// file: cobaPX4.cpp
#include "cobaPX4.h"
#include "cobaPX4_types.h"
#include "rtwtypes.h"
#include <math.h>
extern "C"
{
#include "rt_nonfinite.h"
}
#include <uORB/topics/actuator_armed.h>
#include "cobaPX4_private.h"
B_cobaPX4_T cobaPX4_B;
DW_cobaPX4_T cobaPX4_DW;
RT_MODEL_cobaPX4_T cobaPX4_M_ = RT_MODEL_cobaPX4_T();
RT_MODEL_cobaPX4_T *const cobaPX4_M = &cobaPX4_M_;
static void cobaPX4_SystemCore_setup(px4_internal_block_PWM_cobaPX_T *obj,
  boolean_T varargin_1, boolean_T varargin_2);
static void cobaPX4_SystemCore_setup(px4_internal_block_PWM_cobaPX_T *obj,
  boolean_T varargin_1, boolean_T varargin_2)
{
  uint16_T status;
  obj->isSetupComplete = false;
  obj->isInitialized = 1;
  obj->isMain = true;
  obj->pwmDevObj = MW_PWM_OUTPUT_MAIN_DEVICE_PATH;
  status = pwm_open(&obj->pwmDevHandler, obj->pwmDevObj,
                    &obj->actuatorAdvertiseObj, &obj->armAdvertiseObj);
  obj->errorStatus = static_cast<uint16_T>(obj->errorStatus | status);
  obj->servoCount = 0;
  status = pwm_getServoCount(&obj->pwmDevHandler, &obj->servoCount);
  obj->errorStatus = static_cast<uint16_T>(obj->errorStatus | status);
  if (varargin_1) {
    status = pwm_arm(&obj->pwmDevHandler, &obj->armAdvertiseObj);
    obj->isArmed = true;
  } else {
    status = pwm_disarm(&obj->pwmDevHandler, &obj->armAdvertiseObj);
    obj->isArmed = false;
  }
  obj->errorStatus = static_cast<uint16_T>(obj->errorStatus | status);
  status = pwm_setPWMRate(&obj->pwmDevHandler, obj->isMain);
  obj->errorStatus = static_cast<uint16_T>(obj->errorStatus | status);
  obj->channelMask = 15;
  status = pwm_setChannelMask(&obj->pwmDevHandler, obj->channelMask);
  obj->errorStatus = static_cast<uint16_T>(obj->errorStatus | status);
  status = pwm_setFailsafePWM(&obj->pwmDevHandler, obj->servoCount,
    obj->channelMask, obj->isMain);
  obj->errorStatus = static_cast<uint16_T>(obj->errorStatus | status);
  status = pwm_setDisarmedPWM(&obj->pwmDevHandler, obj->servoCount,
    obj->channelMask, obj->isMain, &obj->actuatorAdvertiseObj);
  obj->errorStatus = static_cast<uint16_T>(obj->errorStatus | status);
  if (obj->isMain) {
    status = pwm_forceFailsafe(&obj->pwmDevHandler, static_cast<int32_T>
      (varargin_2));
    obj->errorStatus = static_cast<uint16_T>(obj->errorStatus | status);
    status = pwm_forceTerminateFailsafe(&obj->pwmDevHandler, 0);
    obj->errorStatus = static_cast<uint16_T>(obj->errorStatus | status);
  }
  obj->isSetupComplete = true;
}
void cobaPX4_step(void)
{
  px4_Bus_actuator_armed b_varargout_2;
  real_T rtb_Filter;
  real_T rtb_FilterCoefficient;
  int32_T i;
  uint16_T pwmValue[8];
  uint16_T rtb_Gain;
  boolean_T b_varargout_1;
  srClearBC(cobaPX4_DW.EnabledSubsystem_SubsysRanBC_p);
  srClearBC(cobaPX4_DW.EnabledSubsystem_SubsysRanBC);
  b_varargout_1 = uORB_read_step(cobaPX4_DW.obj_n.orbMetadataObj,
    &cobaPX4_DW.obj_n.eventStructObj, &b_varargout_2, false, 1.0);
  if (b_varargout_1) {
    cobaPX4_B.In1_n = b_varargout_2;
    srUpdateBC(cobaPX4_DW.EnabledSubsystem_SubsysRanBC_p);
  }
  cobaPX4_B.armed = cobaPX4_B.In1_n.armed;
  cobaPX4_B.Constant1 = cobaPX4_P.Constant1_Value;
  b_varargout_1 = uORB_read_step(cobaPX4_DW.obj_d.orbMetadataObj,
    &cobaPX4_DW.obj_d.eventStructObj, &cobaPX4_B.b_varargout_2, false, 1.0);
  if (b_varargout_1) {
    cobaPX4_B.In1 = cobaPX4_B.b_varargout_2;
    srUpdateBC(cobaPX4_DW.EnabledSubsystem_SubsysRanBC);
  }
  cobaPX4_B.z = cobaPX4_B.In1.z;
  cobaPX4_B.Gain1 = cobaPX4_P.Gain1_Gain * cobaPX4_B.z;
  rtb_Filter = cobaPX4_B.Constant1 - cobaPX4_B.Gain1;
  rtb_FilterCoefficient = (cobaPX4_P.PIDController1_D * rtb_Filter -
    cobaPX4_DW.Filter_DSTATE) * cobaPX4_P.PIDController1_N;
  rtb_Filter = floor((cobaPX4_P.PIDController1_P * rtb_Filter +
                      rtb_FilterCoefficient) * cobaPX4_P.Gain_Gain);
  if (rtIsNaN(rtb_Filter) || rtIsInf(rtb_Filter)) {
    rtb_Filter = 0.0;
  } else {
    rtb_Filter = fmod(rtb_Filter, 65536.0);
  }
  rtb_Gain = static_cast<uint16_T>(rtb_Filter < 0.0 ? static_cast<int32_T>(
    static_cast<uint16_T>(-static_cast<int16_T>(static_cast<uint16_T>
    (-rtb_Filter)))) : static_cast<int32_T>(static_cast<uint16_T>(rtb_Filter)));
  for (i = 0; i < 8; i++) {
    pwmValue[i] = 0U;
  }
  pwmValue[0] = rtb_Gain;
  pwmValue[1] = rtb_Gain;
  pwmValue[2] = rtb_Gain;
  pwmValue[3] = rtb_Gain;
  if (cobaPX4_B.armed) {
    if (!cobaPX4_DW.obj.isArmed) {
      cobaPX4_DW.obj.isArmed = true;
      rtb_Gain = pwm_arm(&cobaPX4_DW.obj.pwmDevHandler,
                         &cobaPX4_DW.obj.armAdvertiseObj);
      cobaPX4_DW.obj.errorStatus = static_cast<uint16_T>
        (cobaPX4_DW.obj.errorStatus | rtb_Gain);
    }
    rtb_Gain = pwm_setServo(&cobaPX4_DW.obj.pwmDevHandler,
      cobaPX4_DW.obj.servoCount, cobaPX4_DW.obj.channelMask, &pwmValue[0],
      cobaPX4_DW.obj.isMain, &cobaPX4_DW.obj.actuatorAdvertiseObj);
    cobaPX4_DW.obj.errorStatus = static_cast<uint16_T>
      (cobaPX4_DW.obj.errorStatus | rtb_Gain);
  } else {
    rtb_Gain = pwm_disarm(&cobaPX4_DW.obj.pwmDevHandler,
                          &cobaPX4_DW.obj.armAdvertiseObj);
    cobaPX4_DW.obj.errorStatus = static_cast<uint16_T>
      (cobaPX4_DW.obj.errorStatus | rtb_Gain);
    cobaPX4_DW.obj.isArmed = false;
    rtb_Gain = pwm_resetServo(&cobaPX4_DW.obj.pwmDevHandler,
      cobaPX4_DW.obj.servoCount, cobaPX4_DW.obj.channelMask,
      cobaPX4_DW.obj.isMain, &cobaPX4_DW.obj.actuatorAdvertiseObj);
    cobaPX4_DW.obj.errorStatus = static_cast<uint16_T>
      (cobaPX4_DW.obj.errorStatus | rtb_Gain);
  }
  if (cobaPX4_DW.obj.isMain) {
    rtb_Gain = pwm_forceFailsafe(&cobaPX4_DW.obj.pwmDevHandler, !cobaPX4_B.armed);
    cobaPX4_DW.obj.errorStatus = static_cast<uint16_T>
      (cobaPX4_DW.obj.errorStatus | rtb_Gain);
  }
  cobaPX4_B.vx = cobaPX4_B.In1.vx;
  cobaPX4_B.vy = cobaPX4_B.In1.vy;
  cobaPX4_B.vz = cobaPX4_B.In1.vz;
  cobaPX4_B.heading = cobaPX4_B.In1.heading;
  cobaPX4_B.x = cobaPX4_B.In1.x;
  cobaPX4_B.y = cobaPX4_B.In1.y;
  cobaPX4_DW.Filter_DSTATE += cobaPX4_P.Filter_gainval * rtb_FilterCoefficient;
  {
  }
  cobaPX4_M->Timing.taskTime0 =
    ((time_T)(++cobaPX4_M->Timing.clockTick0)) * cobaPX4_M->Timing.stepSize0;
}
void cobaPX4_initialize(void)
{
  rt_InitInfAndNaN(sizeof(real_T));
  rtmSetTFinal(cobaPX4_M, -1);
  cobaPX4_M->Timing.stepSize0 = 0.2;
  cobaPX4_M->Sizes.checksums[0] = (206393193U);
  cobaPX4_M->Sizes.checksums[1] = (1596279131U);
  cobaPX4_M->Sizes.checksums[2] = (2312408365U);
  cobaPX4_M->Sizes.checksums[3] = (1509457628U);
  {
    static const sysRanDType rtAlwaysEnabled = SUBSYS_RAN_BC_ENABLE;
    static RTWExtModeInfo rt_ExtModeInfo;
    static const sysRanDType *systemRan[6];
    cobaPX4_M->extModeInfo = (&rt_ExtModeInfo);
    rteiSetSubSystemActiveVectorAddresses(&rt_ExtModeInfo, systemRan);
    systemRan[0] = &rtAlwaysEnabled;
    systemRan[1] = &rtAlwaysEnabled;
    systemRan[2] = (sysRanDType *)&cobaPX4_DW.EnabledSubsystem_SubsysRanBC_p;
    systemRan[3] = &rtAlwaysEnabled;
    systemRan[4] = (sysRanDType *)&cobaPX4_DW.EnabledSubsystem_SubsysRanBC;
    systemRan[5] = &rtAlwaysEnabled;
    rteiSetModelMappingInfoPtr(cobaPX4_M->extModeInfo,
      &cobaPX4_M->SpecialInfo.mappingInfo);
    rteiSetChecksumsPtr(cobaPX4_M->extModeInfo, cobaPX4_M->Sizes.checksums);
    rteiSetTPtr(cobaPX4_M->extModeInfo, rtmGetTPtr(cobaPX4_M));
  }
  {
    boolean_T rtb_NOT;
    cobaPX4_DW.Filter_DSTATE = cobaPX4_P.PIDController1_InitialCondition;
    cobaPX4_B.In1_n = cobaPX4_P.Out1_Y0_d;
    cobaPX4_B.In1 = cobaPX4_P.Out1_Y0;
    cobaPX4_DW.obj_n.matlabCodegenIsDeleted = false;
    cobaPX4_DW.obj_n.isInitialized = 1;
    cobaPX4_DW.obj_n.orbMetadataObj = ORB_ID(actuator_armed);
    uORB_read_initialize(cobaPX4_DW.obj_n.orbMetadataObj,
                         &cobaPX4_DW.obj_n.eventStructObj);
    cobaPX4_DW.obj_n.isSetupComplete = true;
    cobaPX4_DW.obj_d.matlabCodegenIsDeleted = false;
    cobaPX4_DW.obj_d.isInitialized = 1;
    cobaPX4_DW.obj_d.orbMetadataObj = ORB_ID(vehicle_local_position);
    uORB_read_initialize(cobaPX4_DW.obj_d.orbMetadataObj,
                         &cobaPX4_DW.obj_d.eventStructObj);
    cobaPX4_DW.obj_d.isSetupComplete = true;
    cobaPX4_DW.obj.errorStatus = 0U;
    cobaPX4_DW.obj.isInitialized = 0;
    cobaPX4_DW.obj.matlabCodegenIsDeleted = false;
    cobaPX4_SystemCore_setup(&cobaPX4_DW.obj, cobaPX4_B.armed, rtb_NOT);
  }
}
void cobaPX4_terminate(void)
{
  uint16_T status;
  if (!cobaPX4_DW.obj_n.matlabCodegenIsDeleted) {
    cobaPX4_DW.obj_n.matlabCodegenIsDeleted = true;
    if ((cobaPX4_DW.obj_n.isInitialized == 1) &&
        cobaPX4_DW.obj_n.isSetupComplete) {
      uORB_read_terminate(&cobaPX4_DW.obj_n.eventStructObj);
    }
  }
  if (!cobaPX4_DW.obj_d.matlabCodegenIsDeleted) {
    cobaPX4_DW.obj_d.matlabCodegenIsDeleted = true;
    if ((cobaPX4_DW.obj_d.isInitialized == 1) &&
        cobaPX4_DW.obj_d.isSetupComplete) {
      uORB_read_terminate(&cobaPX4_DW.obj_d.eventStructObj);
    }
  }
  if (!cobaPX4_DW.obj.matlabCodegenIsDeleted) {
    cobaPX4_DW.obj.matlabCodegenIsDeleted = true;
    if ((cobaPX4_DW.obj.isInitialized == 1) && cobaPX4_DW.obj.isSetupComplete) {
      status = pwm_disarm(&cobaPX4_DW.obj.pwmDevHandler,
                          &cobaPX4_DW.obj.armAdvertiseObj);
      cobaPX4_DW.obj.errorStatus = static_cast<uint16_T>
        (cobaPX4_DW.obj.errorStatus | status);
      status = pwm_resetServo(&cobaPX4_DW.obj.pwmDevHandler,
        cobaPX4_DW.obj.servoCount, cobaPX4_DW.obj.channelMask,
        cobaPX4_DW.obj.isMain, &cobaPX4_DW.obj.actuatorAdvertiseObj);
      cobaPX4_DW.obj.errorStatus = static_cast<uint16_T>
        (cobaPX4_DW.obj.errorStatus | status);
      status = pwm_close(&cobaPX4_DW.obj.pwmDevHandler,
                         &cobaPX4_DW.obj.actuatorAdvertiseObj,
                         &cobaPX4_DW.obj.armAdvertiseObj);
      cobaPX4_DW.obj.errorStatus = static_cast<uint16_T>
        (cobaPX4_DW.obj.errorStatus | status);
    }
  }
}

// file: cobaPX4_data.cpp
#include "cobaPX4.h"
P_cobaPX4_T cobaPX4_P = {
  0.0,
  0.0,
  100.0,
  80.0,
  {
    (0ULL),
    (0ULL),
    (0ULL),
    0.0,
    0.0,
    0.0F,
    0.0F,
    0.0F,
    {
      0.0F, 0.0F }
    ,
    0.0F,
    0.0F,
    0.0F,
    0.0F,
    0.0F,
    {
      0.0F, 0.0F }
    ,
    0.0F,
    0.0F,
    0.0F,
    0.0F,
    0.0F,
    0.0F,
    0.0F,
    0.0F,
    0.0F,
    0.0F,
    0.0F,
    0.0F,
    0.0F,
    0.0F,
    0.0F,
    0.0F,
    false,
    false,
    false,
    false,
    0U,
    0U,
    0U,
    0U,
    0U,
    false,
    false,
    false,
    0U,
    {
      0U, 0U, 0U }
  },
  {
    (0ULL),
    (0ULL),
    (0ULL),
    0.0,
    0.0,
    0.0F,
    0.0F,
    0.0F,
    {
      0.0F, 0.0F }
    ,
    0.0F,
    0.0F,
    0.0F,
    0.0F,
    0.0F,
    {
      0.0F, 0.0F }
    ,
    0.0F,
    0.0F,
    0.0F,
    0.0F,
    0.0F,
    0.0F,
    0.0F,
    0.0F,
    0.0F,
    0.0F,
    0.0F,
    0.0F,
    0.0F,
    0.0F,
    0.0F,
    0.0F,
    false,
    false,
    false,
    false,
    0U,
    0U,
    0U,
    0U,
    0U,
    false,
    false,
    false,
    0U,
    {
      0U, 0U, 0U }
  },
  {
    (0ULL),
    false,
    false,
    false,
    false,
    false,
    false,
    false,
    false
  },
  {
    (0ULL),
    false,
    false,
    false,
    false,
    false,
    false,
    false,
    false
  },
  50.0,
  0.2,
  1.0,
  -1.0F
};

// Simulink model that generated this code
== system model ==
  PX4PWMOutput#1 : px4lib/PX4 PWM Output  <- 1: BusSelector#1, 2: NOT, 3: Gain, 4: Gain, 5: Gain, 6: Gain
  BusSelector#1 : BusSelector  <- 1: PX4uORBRead#1/2
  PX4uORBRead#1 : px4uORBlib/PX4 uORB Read
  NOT : Logic  Operator=NOT  <- 1: BusSelector#1
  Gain : Gain  <- 1: PIDController1
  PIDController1 : slpidlib/PID Controller  Controller=PD  Form=Parallel  TimeDomain=Discrete-time  IntegratorMethod=Forward Euler  P=80  I=1  D=0  N=100  InitialConditionForIntegrator=0  ExternalReset=none  LimitOutput=off  UpperSaturationLimit=inf  LowerSaturationLimit=-inf  <- 1: Sum#1
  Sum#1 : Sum  Inputs=+-  <- 1: Constant1, 2: Gain1
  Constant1 : Constant  Value=50
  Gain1 : Gain  Gain=-1  <- 1: BusSelector#2/3
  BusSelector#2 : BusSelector  <- 1: PX4uORBRead#2/2
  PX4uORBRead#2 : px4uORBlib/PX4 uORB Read
